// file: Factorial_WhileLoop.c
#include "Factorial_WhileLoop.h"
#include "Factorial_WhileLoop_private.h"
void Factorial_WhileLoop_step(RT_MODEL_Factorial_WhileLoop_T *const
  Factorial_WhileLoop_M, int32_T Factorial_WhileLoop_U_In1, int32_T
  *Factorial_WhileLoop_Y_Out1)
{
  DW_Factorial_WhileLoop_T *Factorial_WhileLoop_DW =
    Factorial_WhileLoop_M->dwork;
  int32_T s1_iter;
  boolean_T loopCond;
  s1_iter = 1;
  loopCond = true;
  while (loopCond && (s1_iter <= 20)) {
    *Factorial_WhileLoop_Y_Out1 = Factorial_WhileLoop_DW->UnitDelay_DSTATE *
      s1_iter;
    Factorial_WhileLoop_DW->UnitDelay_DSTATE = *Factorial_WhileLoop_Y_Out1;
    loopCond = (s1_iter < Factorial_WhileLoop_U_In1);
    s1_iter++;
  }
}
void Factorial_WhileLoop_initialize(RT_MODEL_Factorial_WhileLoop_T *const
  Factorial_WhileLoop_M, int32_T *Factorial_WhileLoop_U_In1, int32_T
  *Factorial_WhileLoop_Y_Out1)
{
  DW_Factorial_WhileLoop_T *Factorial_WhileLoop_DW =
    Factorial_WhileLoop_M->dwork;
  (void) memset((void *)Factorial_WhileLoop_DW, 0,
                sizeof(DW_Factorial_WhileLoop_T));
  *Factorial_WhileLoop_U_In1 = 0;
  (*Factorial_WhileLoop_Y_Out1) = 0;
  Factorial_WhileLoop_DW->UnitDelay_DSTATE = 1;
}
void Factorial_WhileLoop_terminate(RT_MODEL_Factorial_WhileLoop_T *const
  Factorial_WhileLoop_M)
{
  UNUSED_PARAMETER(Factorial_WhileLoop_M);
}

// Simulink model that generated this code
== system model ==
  In1 : Inport
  Out1 : Outport  <- 1: Subsystem#1
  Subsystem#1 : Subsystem  <- 1: In1, 2: Constant#1
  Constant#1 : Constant
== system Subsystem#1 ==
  Inport#1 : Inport
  Inport#2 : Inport
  WhileIterator#1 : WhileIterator  MaxIters=20  <- 1: RelationalOperator#1, 2: Inport#2
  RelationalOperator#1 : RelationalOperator  Operator=<  <- 1: WhileIterator#1, 2: Inport#1
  Outport#1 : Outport  <- 1: Product#1
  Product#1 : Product  <- 1: UnitDelay, 2: WhileIterator#1
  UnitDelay : UnitDelay  InitialCondition=1  <- 1: Product#1
